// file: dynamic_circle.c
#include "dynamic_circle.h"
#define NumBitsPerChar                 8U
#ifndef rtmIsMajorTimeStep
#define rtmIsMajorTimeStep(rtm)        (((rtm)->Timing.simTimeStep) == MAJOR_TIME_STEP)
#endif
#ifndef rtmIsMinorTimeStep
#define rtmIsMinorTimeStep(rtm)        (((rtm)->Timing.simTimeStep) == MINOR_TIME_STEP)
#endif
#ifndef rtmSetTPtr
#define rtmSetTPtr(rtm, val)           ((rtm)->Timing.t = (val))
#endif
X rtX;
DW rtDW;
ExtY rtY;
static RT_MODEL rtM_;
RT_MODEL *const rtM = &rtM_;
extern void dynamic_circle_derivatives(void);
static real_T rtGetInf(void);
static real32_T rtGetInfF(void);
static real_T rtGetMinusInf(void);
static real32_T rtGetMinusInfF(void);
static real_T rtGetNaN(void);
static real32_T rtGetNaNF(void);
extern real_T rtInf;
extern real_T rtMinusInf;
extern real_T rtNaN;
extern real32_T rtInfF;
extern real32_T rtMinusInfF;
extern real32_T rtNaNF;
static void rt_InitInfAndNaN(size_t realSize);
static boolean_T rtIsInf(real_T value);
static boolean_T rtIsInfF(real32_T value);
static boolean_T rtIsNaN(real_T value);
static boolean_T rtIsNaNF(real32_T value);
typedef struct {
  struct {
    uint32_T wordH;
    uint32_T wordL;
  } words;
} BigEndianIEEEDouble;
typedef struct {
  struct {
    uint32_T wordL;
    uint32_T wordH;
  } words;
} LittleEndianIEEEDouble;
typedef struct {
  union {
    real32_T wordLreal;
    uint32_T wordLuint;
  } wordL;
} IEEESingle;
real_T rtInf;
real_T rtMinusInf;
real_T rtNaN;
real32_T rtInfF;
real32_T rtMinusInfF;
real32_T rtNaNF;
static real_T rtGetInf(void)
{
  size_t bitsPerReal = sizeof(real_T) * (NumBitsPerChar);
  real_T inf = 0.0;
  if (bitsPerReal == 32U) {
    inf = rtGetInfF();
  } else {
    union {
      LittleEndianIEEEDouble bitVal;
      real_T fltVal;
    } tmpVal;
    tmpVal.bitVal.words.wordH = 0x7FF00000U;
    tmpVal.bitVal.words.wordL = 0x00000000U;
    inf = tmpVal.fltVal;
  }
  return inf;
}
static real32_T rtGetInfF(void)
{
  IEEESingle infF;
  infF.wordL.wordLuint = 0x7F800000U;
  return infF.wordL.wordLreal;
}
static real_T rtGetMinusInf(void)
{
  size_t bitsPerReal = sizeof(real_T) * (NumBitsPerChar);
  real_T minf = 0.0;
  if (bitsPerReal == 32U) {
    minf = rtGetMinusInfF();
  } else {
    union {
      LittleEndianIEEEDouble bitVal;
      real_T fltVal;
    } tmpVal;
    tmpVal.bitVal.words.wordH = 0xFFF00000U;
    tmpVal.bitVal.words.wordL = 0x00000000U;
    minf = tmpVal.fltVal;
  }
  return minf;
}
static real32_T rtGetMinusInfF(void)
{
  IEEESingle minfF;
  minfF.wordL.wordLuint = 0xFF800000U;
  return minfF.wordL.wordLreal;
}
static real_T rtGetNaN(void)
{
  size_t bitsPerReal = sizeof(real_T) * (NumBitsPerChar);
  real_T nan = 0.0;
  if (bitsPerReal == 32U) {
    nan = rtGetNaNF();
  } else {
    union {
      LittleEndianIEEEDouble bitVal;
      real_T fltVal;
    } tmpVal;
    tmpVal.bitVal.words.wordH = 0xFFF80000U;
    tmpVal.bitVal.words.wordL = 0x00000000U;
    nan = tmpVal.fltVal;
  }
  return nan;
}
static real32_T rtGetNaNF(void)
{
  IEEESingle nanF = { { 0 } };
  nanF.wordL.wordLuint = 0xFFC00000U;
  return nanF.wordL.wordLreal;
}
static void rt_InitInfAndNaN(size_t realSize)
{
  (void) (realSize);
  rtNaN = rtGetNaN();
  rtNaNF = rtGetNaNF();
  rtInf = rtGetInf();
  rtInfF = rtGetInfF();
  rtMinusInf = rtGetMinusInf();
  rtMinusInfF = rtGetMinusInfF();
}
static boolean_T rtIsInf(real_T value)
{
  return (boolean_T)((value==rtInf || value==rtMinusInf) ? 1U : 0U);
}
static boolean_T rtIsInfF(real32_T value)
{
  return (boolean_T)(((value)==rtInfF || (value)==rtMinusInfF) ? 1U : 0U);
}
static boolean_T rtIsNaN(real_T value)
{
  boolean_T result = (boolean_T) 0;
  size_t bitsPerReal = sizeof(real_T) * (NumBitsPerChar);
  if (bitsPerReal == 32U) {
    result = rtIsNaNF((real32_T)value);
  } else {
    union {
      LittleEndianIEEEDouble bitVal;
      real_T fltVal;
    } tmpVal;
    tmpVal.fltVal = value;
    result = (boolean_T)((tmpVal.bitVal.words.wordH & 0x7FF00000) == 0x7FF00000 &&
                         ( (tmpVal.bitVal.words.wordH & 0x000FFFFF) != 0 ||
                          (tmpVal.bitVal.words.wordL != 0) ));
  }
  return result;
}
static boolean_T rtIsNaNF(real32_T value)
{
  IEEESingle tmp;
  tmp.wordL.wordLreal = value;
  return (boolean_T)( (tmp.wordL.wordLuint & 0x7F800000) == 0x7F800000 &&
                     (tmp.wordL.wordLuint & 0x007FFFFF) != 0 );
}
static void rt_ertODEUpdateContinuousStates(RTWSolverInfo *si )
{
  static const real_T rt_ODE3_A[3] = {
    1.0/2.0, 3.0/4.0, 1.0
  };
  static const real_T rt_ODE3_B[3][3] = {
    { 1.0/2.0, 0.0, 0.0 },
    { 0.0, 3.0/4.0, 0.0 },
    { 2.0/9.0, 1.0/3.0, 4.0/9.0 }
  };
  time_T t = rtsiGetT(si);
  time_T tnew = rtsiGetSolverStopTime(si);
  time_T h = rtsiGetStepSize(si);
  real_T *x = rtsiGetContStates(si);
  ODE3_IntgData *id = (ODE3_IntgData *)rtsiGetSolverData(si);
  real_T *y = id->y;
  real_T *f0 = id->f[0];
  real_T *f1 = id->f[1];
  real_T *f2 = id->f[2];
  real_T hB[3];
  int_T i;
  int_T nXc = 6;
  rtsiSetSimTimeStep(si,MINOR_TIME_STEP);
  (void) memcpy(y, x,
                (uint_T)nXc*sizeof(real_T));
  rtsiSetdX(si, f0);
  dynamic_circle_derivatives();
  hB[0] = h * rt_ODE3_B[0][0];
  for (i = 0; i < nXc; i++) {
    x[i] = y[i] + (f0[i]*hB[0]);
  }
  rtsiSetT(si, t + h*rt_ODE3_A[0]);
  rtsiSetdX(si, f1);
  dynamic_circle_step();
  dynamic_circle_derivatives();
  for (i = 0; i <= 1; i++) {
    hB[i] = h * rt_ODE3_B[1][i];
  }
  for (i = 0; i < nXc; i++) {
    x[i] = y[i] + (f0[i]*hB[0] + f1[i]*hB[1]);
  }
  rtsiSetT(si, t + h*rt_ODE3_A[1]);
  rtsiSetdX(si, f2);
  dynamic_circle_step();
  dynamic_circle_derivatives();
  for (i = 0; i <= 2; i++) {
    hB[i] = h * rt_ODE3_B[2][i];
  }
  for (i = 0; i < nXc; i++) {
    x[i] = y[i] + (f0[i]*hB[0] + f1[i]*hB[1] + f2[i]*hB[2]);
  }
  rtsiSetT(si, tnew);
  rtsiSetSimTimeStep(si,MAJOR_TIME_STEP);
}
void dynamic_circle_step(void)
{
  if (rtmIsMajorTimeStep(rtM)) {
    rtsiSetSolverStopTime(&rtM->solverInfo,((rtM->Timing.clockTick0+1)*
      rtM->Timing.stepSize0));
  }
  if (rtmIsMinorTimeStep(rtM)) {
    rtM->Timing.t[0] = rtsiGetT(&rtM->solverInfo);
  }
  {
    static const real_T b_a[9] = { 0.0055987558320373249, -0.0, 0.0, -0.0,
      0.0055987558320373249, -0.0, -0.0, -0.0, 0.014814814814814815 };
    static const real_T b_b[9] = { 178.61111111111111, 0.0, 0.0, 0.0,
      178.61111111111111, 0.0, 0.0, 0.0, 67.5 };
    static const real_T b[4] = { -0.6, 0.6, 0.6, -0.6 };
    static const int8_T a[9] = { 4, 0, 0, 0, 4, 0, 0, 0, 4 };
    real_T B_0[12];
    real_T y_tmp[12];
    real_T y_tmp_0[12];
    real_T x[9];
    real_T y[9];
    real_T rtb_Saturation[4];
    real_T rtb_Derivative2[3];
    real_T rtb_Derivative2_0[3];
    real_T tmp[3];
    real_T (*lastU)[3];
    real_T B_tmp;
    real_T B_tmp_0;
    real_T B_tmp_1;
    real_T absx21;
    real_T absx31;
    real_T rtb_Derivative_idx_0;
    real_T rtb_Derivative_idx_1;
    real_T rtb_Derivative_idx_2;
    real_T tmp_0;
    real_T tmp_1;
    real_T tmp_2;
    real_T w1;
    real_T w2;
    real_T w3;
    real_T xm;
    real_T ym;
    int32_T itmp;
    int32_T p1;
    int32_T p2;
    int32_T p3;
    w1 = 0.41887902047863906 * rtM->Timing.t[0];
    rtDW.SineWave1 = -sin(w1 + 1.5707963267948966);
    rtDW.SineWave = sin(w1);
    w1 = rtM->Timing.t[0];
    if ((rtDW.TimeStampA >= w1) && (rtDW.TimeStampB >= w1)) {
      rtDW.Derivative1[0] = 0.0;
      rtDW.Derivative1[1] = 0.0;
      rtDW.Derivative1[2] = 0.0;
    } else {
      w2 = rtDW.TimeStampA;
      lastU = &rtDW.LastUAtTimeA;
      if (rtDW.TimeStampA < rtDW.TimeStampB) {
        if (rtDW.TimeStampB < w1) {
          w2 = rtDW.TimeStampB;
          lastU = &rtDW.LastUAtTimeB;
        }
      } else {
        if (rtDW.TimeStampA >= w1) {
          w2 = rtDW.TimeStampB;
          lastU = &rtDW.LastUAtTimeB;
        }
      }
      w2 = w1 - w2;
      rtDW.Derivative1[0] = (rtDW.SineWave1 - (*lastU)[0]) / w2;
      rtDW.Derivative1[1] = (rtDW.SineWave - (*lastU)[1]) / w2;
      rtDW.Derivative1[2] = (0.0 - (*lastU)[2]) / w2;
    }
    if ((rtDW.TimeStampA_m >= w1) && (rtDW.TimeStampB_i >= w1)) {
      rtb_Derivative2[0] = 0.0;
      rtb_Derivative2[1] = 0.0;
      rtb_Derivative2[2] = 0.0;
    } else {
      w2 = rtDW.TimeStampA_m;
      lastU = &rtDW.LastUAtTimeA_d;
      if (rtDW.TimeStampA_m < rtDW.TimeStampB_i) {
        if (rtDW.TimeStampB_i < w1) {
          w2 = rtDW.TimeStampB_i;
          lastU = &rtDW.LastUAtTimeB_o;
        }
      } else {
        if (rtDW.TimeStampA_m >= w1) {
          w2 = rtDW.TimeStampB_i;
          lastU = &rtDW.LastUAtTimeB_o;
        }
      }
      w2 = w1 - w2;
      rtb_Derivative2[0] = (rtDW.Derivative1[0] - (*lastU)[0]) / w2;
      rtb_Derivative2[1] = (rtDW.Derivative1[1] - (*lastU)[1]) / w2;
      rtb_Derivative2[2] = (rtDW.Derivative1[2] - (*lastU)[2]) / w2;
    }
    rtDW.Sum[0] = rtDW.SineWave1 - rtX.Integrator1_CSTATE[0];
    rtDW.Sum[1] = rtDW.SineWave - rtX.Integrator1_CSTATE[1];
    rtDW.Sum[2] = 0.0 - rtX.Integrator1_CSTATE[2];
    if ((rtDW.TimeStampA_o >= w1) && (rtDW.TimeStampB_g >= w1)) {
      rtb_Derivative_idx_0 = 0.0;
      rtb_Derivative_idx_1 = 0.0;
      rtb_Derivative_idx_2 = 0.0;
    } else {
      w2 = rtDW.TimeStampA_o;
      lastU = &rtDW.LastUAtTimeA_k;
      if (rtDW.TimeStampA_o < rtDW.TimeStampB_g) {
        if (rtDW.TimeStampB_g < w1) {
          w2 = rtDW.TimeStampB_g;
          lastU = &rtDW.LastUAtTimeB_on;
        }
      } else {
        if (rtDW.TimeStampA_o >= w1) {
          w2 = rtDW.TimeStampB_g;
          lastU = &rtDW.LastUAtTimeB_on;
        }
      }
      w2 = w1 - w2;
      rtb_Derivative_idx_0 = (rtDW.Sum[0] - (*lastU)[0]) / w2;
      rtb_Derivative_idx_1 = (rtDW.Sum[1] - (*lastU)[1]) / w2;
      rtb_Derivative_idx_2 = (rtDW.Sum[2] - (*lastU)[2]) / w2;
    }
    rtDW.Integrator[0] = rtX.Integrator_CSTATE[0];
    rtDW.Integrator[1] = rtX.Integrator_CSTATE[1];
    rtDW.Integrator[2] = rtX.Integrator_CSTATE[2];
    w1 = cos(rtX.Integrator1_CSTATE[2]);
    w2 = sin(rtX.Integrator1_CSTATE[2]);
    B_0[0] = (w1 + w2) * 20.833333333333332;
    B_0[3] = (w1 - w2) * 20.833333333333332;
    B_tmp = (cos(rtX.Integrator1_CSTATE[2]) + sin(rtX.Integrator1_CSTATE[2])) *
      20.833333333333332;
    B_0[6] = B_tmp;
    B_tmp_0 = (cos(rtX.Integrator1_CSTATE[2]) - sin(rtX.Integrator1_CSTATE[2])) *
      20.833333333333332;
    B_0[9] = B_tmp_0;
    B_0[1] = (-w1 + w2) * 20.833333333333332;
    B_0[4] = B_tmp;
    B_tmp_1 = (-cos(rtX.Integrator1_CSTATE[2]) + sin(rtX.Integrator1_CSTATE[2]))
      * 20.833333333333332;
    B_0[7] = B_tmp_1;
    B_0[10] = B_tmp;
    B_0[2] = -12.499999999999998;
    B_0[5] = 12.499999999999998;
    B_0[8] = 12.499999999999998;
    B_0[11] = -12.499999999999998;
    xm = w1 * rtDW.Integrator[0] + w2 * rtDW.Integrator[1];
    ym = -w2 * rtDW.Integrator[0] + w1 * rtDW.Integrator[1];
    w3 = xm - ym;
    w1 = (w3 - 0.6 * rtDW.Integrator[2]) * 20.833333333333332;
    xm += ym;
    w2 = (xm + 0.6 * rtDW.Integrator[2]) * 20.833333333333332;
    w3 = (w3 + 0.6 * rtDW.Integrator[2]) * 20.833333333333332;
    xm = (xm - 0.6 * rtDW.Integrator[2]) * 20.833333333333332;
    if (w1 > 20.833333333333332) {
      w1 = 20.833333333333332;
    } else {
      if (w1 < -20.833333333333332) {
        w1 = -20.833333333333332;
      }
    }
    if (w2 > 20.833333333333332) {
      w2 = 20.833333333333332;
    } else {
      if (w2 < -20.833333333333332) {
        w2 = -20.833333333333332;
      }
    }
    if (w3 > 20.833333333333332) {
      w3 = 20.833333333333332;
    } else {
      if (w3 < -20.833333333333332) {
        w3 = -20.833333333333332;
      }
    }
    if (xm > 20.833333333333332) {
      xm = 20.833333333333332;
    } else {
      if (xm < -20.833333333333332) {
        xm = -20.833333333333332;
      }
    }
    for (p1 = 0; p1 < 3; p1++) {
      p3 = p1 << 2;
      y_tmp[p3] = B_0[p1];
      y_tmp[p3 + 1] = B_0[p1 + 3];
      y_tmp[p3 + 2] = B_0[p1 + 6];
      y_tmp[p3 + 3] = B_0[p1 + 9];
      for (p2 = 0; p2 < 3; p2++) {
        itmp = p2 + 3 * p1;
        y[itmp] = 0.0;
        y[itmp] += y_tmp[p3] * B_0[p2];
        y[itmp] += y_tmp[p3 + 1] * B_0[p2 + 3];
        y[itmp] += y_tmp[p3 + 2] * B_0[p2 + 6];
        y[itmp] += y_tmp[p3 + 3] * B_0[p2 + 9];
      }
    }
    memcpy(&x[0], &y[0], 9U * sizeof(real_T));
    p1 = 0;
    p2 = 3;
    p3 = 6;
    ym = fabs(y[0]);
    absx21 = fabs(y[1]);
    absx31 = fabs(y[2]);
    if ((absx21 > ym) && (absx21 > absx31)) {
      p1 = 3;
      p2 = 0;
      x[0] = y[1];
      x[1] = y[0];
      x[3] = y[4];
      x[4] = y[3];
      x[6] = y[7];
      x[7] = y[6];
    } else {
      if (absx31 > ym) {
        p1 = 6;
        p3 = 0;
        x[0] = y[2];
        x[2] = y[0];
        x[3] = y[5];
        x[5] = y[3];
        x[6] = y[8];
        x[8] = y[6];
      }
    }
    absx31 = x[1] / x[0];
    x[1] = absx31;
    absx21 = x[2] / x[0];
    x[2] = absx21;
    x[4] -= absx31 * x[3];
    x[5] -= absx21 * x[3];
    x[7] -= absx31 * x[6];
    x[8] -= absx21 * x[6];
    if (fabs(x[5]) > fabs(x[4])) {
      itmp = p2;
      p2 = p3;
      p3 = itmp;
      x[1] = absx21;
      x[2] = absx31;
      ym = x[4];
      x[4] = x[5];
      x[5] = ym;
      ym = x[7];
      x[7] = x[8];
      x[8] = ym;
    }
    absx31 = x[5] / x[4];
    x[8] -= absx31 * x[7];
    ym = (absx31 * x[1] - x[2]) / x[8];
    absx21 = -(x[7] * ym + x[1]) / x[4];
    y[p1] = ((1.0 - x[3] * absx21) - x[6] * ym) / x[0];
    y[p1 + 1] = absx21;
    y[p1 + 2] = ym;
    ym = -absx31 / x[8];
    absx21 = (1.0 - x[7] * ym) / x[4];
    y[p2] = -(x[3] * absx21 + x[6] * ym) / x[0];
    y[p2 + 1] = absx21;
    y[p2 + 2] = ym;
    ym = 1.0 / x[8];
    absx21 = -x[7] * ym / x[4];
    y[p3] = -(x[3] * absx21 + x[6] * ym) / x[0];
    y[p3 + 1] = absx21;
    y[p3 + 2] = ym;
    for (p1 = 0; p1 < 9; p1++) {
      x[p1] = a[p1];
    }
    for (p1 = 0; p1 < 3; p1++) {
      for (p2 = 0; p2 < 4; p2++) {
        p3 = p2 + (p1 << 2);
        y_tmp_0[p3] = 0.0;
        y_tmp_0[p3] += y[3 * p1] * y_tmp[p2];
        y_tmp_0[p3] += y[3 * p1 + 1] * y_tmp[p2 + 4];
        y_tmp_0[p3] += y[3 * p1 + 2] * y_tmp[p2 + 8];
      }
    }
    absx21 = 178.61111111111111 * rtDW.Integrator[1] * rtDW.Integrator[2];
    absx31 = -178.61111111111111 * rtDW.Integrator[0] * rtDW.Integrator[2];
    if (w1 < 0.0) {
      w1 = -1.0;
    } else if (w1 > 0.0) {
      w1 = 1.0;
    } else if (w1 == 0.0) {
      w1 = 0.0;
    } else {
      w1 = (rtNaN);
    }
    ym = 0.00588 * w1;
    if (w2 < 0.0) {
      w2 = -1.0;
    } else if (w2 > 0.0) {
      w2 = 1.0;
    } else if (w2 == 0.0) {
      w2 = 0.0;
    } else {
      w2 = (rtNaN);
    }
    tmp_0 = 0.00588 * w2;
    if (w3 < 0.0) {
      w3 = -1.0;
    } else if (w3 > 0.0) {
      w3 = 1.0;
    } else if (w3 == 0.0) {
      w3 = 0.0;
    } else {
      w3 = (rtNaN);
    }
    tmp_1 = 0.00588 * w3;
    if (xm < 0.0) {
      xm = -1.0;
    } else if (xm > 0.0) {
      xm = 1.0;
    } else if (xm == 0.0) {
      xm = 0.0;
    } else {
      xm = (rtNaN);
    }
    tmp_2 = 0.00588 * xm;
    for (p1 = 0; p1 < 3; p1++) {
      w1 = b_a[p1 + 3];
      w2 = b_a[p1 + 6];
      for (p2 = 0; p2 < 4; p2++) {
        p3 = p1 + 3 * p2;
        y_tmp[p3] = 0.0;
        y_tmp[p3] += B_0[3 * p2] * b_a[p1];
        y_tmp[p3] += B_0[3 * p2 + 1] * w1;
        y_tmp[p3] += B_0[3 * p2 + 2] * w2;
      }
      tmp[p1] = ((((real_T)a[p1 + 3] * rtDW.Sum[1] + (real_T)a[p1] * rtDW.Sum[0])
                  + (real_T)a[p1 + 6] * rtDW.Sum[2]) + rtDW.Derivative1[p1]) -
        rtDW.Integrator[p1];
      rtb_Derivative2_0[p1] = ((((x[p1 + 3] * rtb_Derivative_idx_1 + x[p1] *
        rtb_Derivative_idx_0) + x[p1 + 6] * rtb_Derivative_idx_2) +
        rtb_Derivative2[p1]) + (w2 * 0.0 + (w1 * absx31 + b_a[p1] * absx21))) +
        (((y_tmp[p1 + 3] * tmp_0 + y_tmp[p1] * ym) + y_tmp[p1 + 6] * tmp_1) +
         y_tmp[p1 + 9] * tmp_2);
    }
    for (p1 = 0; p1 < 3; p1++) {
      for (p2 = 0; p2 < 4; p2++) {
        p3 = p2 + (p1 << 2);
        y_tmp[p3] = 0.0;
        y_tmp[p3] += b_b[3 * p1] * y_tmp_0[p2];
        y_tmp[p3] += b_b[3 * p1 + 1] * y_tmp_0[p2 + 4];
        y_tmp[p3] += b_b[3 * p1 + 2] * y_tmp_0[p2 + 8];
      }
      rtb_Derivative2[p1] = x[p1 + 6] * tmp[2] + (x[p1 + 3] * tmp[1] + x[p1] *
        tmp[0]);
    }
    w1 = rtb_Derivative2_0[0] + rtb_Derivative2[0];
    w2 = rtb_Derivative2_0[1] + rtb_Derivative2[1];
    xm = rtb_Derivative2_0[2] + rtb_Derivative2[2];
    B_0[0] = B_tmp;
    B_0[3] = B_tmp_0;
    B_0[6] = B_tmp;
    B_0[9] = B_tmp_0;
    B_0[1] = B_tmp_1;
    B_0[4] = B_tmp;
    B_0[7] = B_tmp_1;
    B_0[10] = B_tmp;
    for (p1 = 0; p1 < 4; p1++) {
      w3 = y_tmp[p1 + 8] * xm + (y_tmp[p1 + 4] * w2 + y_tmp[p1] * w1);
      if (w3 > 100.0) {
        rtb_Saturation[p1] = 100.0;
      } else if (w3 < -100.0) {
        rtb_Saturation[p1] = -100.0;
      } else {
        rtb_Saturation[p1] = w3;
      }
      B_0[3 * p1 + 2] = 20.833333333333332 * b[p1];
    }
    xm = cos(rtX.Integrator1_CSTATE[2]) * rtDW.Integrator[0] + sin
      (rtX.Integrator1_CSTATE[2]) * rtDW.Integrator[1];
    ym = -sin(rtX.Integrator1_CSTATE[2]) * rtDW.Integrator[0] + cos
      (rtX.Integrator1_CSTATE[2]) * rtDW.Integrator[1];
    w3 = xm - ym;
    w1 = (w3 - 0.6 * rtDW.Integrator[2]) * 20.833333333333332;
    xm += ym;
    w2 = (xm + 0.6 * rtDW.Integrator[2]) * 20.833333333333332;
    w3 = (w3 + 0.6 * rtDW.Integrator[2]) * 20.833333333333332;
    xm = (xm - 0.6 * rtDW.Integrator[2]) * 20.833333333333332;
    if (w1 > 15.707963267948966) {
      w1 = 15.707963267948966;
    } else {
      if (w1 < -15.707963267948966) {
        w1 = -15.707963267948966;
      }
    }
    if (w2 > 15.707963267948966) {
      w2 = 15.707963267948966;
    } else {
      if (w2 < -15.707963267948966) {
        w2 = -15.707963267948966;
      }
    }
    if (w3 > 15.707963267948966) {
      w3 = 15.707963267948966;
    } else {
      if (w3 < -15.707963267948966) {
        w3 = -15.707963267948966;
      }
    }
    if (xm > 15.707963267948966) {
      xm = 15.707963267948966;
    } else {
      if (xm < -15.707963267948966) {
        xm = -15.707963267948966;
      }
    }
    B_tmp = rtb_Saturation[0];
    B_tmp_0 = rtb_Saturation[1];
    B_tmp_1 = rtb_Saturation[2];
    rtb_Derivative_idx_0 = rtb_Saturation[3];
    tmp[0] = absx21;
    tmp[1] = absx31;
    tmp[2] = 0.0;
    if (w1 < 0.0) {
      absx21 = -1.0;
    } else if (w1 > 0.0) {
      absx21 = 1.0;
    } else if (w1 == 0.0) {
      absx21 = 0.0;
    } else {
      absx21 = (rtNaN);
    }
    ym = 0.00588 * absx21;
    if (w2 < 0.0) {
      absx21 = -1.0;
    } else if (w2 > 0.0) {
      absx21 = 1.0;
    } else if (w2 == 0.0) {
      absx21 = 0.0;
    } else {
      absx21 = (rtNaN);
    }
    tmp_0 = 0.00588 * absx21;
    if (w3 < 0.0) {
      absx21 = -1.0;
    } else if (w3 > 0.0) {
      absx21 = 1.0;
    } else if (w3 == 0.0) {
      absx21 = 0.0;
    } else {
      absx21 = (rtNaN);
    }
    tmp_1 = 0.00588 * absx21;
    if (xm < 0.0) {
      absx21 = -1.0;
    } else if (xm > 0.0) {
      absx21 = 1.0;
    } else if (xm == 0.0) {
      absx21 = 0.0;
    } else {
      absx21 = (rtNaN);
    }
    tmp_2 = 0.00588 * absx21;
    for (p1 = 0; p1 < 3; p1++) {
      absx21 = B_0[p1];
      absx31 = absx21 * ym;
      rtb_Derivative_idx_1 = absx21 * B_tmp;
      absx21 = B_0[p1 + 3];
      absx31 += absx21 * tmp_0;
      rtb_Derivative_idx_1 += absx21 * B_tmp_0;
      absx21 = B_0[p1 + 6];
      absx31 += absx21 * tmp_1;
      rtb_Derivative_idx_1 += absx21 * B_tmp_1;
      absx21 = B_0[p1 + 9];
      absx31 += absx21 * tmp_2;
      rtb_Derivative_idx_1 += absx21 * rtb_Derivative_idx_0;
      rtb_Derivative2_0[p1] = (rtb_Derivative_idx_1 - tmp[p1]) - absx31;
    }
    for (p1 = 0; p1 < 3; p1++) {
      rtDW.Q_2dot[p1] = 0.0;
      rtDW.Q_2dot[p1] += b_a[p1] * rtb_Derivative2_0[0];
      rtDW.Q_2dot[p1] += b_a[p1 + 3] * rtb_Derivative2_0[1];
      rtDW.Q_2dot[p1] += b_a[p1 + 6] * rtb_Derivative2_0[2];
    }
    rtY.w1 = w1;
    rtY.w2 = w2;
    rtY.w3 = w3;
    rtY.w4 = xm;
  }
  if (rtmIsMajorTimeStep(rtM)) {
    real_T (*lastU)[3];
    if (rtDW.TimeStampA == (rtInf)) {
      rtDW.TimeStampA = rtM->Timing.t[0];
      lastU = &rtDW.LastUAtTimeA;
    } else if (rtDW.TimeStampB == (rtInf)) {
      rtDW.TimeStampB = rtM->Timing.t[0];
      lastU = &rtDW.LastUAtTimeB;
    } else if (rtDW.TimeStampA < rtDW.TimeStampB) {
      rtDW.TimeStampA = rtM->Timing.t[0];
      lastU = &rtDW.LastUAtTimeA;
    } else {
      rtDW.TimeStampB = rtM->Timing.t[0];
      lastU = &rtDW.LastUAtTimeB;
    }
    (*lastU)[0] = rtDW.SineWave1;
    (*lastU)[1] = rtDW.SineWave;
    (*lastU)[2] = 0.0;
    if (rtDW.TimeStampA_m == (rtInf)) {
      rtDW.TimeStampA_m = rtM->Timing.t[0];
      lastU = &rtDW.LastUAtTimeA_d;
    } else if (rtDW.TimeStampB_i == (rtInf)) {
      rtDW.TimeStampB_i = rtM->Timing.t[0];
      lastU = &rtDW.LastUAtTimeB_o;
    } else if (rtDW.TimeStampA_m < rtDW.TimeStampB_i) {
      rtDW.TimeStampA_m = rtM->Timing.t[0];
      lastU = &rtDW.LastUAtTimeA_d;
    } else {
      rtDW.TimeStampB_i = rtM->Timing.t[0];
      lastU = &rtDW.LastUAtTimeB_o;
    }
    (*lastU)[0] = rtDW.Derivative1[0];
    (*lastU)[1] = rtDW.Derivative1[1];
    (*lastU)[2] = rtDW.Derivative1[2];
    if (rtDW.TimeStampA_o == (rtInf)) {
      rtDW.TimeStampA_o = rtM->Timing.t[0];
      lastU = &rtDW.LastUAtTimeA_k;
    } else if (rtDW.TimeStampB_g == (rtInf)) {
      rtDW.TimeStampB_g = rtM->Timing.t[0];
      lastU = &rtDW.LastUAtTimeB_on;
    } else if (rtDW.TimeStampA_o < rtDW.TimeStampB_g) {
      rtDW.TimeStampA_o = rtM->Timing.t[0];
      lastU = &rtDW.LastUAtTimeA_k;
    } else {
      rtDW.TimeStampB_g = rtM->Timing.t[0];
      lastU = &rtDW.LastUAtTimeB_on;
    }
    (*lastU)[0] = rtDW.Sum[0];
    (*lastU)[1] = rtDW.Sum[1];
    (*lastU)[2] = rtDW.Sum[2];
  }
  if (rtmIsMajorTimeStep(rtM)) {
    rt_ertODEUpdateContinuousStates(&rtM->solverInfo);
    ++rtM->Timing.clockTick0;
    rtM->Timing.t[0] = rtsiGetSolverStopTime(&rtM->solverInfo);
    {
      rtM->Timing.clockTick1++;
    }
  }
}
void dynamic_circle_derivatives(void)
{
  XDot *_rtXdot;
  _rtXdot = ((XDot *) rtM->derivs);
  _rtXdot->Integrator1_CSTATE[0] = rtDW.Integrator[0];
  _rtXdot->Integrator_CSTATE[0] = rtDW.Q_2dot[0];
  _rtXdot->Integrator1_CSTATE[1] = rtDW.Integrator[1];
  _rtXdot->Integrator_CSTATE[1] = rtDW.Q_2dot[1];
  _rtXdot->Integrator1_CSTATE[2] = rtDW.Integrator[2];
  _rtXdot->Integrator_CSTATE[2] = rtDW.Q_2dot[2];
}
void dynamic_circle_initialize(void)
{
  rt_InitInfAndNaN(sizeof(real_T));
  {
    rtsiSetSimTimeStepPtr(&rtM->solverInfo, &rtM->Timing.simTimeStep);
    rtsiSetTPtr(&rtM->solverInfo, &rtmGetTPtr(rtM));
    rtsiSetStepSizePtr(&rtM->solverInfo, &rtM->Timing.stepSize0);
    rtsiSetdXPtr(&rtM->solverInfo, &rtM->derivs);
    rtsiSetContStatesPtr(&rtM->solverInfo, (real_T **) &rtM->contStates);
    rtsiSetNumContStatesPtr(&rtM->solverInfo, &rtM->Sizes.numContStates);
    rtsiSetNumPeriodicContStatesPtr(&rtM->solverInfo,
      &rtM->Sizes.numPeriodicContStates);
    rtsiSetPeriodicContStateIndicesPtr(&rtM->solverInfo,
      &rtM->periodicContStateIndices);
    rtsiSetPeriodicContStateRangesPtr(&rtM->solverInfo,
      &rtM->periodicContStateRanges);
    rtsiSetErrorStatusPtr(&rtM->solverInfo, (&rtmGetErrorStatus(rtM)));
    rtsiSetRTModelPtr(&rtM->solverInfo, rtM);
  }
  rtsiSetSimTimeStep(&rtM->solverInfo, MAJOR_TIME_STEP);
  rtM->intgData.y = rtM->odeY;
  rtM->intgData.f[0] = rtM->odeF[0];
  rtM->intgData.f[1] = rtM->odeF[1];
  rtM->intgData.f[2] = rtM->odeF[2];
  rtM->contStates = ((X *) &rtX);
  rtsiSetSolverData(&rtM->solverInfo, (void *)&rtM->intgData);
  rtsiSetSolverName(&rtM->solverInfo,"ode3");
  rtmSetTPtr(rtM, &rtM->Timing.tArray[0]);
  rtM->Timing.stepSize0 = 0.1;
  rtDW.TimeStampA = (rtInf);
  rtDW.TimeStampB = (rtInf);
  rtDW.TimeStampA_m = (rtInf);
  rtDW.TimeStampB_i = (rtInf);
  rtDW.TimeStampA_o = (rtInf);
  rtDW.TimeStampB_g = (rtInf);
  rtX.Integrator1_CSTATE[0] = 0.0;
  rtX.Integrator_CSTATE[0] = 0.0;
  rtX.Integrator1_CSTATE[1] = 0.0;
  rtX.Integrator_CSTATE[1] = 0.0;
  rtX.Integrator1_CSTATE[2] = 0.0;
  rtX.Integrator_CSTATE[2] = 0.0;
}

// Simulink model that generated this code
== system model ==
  w1 : Outport  <- 1: MATLABFunction#1/2
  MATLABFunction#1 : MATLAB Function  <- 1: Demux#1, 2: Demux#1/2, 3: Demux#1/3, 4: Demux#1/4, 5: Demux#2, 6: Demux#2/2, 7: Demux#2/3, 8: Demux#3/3
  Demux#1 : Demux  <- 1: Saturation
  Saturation : Saturate  UpperLimit=100  LowerLimit=-100  <- 1: MATLABFunction#2
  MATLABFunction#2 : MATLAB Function  <- 1: Derivative2, 2: Derivative, 3: MATLABFunction#3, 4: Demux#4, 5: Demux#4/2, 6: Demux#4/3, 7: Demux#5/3
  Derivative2 : Derivative  <- 1: Derivative1
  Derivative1 : Derivative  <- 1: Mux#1
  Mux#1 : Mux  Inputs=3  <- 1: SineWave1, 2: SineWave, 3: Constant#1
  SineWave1 : Sin  Amplitude=-1  Frequency=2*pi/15  Phase=pi/2
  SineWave : Sin  Frequency=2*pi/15
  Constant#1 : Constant  Value=0
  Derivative : Derivative  <- 1: Sum
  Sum : Sum  Inputs=+-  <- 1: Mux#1, 2: Integrator1
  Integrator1 : Integrator  <- 1: Integrator
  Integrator : Integrator  <- 1: MATLABFunction#1
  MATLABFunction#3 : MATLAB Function  <- 1: Derivative1, 2: Integrator, 3: Sum
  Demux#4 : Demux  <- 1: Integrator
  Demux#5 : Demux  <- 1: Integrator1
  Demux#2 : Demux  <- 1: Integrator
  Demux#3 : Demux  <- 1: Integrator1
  w2 : Outport  <- 1: MATLABFunction#1/3
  w3 : Outport  <- 1: MATLABFunction#1/4
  w4 : Outport  <- 1: MATLABFunction#1/5
== matlab function MATLABFunction#1 ==
function [Q_2dot,w1,w2,w3,w4]  = fcn(T1, T2, T3, T4,x_dot,y_dot,theta_dot,theta)
m=5;
I=5;
Ib=0.1;
l1= 0.3;
l2=0.3;
r=0.048;
g=9.8;
u=0.01;
N = m*g/4;
M=[(m+4*Ib/(r*r)) 0 0; 0 (m+4*Ib/(r*r)) 0; 0 0 (I+4*Ib*(l1+l2)*(l1+l2)/(r*r))];
C= [(m+4*Ib/(r*r))*y_dot*theta_dot;-(m+4*Ib/(r*r))*x_dot*theta_dot;0 ];
B=(1/r)*[(cos(theta)+sin(theta)) (cos(theta)-sin(theta)) (cos(theta)+sin(theta)) (cos(theta)-sin(theta));
         (-cos(theta)+sin(theta)) (cos(theta)+sin(theta)) (-cos(theta)+sin(theta)) (cos(theta)+sin(theta)); 
         (-(l1+l2)) (l1+l2) (l1+l2) (-(l1+l2)) ];
T=[T1;T2;T3;T4];
xm= cos(theta)*x_dot+sin(theta)*y_dot;
ym= -sin(theta)*x_dot+cos(theta)*y_dot;
w1 = (1/r)*(xm-ym-(l1+l2)*theta_dot);
w2 = (1/r)*(xm+ym+(l1+l2)*theta_dot);
w3 = (1/r)*(xm-ym+(l1+l2)*theta_dot);
w4 = (1/r)*(xm+ym-(l1+l2)*theta_dot);
w_max = 5*pi;
if w1 > w_max
    w1 = w_max; %w = 20.83
elseif w1 < -w_max
    w1 = -w_max;
end
if w2 > w_max
    w2 = w_max;
elseif w2 < -w_max
    w2 = -w_max;
end
if w3 > w_max
    w3 = w_max;
elseif w3 < -w_max
    w3 = -w_max;
end
if w4 > w_max
    w4 = w_max;
elseif w4 < -w_max
    w4 = -w_max;
end
Xi=[u*r*N*sign(w1);u*r*N*sign(w2);u*r*N*sign(w3);u*N*r*sign(w4)];

Q_2dot=inv(M)*(B*T-C-B*Xi);

== matlab function MATLABFunction#2 ==
function u_control = fcn(Qr_2dot,e1_dot,e2,x_dot,y_dot,theta_dot,theta)

m=5;
I=5;
Ib=0.1;
l1= 0.3;
l2=0.3;
r=0.048;
g=9.8;
u=0.01;
N = m*g/4;
M=[(m+4*Ib/(r*r)) 0 0; 0 (m+4*Ib/(r*r)) 0; 0 0 (I+4*Ib*(l1+l2)*(l1+l2)/(r*r))];
C= [(m+4*Ib/(r*r))*y_dot*theta_dot;-(m+4*Ib/(r*r))*x_dot*theta_dot;0 ];
B=(1/r)*[(cos(theta)+sin(theta)) (cos(theta)-sin(theta)) (cos(theta)+sin(theta)) (cos(theta)-sin(theta));
    (-cos(theta)+sin(theta)) (cos(theta)+sin(theta)) (-cos(theta)+sin(theta)) (cos(theta)+sin(theta)); 
    (-(l1+l2)) (l1+l2) (l1+l2) (-(l1+l2)) ];

xm= cos(theta)*x_dot+sin(theta)*y_dot;
ym= -sin(theta)*x_dot+cos(theta)*y_dot;
w1 = (1/r)*(xm-ym-(l1+l2)*theta_dot);
w2 = (1/r)*(xm+ym+(l1+l2)*theta_dot);
w3 = (1/r)*(xm-ym+(l1+l2)*theta_dot);
w4 = (1/r)*(xm+ym-(l1+l2)*theta_dot);
if w1 > 1/r
    w1 = 1/r; %w = 20.83
elseif w1 < -1/r
    w1 = -1/r;
end
if w2 > 1/r
    w2 = 1/r;
elseif w2 < -1/r
    w2 = -1/r;
end
if w3 > 1/r
    w3 = 1/r;
elseif w3 < -1/r
    w3 = -1/r;
end
if w4 > 1/r
    w4 = 1/r;
elseif w4 < -1/r
    w4 = -1/r;
end
Xi=[u*r*N*sign(w1);u*r*N*sign(w2);u*r*N*sign(w3);u*N*r*sign(w4)];

k1 = [4 0 0;
      0 4 0;
      0 0 4];
k2 = [4 0 0;
      0 4 0;
      0 0 4];
  
u_control = B'*inv(B*B')*M*((Qr_2dot+k1*e1_dot)+inv(M)*C+inv(M)*B*Xi+k2*e2);

== matlab function MATLABFunction#3 ==
function e2  = fcn(Qr_dot,Q_dot,e1)

k1 = [4 0 0;
      0 4 0;
      0 0 4];
 
%x2r_dot = (Qr_2dot+k1*e1_dot);
x2r = Qr_dot + k1*e1;
e2 = x2r - Q_dot;
